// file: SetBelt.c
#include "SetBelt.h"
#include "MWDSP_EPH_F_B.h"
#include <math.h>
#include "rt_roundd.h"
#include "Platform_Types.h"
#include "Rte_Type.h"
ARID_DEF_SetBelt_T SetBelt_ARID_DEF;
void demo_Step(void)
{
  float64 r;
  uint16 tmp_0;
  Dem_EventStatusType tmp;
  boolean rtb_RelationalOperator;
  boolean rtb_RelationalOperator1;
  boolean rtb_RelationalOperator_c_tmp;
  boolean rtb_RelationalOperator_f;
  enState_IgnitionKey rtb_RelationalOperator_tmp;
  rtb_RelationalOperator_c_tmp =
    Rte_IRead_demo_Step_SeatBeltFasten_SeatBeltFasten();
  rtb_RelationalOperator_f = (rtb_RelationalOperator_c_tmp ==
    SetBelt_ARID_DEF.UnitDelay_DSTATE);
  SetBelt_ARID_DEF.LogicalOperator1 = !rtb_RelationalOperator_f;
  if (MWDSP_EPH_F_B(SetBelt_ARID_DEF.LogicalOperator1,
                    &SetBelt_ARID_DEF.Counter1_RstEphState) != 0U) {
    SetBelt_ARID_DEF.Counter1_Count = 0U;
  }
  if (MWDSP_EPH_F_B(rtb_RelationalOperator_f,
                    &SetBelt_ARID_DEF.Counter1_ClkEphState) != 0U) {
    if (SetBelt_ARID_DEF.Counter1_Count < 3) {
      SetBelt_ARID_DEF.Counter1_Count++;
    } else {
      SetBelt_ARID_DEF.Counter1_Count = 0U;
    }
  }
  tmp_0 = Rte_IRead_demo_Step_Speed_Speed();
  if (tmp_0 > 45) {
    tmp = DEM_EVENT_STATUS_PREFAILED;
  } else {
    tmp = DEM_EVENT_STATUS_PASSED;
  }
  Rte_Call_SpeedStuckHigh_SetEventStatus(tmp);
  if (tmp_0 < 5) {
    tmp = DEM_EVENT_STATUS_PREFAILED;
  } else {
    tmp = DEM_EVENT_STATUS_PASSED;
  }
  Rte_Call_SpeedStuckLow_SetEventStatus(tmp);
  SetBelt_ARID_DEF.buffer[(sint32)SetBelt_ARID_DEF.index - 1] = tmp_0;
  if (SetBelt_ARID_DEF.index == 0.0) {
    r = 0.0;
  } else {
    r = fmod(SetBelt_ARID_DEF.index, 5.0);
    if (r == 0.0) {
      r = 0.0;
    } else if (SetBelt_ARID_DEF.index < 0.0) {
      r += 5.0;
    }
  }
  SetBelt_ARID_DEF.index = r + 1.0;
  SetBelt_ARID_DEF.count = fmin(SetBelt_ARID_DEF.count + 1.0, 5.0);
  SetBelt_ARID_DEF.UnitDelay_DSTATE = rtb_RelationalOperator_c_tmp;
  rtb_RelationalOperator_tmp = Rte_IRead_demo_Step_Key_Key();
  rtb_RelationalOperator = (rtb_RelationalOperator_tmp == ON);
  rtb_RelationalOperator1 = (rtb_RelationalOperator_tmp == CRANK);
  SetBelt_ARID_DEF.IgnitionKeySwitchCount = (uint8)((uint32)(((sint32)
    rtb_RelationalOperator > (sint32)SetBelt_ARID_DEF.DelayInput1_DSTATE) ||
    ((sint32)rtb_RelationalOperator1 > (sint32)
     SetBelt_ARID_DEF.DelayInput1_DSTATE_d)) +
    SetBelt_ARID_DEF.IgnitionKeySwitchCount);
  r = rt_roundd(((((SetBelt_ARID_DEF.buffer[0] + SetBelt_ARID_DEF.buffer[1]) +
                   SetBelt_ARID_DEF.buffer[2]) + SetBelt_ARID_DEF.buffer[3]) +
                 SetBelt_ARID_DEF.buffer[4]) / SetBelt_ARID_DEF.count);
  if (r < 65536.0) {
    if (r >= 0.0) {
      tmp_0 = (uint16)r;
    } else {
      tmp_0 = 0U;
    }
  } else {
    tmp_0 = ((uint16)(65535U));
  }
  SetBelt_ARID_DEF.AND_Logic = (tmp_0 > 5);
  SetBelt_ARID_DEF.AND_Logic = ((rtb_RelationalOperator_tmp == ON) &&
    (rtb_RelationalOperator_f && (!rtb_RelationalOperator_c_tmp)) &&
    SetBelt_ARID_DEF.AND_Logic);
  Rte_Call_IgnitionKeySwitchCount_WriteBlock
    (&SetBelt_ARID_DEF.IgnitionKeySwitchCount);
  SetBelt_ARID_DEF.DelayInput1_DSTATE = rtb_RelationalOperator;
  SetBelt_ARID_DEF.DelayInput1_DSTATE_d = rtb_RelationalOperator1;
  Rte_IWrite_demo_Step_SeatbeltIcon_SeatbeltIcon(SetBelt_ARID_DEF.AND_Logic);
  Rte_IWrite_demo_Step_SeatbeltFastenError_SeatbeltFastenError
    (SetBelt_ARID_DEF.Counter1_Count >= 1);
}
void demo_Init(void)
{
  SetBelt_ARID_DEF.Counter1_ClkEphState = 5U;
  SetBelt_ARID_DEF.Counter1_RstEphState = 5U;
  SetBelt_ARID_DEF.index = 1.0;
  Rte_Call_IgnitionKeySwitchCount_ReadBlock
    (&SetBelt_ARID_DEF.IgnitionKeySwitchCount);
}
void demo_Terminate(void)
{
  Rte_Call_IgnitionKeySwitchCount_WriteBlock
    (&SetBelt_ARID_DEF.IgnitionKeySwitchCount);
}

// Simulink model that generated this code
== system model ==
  Inport#1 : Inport
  Inport#2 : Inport
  Inport#3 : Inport
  Outport#1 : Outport  <- 1: Subsystem#1
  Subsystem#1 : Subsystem  <- 1: Inport#1, 2: Subsystem#2, 3: Subsystem#2/3, Trigger: FunctionCallGenerator#1
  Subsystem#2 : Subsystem  <- 1: Inport#2, 2: Inport#3, Trigger: FunctionCallGenerator#2
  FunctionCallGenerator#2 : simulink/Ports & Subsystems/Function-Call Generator
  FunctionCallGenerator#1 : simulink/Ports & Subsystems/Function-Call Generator
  Outport#2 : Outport  <- 1: Subsystem#2/2
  Subsystem#3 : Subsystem
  Subsystem#4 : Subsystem
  DataStoreMemory#1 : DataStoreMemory  DataStoreName=IgnitionKeySwitchCount
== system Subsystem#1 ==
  Inport#4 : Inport
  SeatBeltFasten : Inport
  Speed : Inport
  TriggerPort#1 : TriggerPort  TriggerType=function-call
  Outport#3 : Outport  <- 1: AND_Logic
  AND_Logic : Logic  Inputs=3  <- 1: RelationalOperator, 2: Logic#1, 3: RelationalOperator#1
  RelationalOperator : RelationalOperator  Operator===  <- 1: Inport#4, 2: Constant#1
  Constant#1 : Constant  Value=enState_IgnitionKey.ON
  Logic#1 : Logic  Operator=NOT  <- 1: SeatBeltFasten
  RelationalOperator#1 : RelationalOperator  Operator=>  <- 1: Speed, 2: Constant#2
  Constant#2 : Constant  Value=5
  DataStoreWrite#1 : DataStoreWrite  DataStoreName=IgnitionKeySwitchCount  Indices=1  <- 1: Sum#1
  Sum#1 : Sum  <- 1: Logic#2, 2: DataStoreRead#1
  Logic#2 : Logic  Operator=OR  <- 1: DetectIncrease#1, 2: DetectIncrease#2
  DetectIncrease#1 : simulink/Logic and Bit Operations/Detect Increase  <- 1: RelationalOperator#2
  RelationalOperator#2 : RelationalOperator  Operator===  <- 1: Inport#4, 2: Constant#3
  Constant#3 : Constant  Value=enState_IgnitionKey.ON
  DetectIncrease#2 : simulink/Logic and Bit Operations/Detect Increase  <- 1: RelationalOperator1
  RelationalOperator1 : RelationalOperator  Operator===  <- 1: Inport#4, 2: Constant#4
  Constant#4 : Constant  Value=enState_IgnitionKey.CRANK
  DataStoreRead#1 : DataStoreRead  DataStoreName=IgnitionKeySwitchCount  Indices=1
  NvMServiceCaller#1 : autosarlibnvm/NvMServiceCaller  <- 1: DataStoreRead#2
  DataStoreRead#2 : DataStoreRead  DataStoreName=IgnitionKeySwitchCount  Indices=1
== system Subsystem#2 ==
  Inport#5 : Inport
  Inport#6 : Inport
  TriggerPort#2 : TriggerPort  TriggerType=function-call
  Outport#4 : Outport  <- 1: Switch#1
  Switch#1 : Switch  Criteria=u2 ~= 0  <- 1: Inport#5, 2: RelationalOperator#3, 3: Constant#5
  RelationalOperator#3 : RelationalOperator  Operator===  <- 1: Inport#5, 2: UnitDelay
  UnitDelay : UnitDelay  <- 1: Inport#5
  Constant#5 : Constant
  Outport#5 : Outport  <- 1: CompareToConstant#1
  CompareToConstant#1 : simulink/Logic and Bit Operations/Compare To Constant  relop=>=  const=1  <- 1: Counter1
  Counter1 : dspswit3/Counter  <- 1: RelationalOperator#3, 2: LogicalOperator1
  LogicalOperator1 : Logic  Operator=NOT  <- 1: RelationalOperator#3
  Outport#6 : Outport  <- 1: MATLABFunction#1
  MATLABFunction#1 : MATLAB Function  <- 1: Inport#6
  DiagnosticMonitorCaller#1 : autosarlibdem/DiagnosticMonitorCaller  <- 1: Switch#2
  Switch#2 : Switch  Criteria=u2 ~= 0  <- 1: DEM_EVENT_STATUS_PREFAILED, 2: CompareToConstant#2, 3: DEM_EVENT_STATUS_PASSED
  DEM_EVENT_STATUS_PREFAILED : Constant  Value=Dem_EventStatusType.DEM_EVENT_STATUS_PREFAILED
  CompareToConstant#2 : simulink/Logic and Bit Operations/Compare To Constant  relop=>  const=45  <- 1: Inport#6
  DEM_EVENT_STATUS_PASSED : Constant  Value=Dem_EventStatusType.DEM_EVENT_STATUS_PASSED
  DiagnosticMonitorCaller#2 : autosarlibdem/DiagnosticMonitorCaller  <- 1: Switch#3
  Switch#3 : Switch  Criteria=u2 ~= 0  <- 1: Constant#6, 2: CompareToConstant#3, 3: Constant#7
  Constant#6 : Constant  Value=Dem_EventStatusType.DEM_EVENT_STATUS_PREFAILED
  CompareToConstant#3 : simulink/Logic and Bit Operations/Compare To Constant  relop=<  const=5  <- 1: Inport#6
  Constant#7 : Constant  Value=Dem_EventStatusType.DEM_EVENT_STATUS_PASSED
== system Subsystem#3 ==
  DataStoreWrite#2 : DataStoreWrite  DataStoreName=IgnitionKeySwitchCount  Indices=1  <- 1: NvMServiceCaller#2
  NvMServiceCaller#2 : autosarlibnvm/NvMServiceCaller
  EventListener#1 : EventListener
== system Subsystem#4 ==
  NvMServiceCaller#3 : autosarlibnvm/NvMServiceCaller  <- 1: DataStoreRead#3
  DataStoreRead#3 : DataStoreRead  DataStoreName=IgnitionKeySwitchCount  Indices=1
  EventListener#2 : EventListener
== matlab function MATLABFunction#1 ==
function avg_out = runningAverage(speed)
%#codegen

    persistent buffer index count

    N = 5;  

    if isempty(buffer)
        buffer = zeros(1, N);  % Buffer 5 phần tử
        index = 1;             % Vị trí ghi đầu tiên
        count = 0;             % Số lượng phần tử đã ghi
    end

    buffer(index) = double(speed);
    index = mod(index, N) + 1;
    count = min(count + 1, N);

    % Tính trung bình
    avg_out = uint16(sum(buffer) / count);
end
